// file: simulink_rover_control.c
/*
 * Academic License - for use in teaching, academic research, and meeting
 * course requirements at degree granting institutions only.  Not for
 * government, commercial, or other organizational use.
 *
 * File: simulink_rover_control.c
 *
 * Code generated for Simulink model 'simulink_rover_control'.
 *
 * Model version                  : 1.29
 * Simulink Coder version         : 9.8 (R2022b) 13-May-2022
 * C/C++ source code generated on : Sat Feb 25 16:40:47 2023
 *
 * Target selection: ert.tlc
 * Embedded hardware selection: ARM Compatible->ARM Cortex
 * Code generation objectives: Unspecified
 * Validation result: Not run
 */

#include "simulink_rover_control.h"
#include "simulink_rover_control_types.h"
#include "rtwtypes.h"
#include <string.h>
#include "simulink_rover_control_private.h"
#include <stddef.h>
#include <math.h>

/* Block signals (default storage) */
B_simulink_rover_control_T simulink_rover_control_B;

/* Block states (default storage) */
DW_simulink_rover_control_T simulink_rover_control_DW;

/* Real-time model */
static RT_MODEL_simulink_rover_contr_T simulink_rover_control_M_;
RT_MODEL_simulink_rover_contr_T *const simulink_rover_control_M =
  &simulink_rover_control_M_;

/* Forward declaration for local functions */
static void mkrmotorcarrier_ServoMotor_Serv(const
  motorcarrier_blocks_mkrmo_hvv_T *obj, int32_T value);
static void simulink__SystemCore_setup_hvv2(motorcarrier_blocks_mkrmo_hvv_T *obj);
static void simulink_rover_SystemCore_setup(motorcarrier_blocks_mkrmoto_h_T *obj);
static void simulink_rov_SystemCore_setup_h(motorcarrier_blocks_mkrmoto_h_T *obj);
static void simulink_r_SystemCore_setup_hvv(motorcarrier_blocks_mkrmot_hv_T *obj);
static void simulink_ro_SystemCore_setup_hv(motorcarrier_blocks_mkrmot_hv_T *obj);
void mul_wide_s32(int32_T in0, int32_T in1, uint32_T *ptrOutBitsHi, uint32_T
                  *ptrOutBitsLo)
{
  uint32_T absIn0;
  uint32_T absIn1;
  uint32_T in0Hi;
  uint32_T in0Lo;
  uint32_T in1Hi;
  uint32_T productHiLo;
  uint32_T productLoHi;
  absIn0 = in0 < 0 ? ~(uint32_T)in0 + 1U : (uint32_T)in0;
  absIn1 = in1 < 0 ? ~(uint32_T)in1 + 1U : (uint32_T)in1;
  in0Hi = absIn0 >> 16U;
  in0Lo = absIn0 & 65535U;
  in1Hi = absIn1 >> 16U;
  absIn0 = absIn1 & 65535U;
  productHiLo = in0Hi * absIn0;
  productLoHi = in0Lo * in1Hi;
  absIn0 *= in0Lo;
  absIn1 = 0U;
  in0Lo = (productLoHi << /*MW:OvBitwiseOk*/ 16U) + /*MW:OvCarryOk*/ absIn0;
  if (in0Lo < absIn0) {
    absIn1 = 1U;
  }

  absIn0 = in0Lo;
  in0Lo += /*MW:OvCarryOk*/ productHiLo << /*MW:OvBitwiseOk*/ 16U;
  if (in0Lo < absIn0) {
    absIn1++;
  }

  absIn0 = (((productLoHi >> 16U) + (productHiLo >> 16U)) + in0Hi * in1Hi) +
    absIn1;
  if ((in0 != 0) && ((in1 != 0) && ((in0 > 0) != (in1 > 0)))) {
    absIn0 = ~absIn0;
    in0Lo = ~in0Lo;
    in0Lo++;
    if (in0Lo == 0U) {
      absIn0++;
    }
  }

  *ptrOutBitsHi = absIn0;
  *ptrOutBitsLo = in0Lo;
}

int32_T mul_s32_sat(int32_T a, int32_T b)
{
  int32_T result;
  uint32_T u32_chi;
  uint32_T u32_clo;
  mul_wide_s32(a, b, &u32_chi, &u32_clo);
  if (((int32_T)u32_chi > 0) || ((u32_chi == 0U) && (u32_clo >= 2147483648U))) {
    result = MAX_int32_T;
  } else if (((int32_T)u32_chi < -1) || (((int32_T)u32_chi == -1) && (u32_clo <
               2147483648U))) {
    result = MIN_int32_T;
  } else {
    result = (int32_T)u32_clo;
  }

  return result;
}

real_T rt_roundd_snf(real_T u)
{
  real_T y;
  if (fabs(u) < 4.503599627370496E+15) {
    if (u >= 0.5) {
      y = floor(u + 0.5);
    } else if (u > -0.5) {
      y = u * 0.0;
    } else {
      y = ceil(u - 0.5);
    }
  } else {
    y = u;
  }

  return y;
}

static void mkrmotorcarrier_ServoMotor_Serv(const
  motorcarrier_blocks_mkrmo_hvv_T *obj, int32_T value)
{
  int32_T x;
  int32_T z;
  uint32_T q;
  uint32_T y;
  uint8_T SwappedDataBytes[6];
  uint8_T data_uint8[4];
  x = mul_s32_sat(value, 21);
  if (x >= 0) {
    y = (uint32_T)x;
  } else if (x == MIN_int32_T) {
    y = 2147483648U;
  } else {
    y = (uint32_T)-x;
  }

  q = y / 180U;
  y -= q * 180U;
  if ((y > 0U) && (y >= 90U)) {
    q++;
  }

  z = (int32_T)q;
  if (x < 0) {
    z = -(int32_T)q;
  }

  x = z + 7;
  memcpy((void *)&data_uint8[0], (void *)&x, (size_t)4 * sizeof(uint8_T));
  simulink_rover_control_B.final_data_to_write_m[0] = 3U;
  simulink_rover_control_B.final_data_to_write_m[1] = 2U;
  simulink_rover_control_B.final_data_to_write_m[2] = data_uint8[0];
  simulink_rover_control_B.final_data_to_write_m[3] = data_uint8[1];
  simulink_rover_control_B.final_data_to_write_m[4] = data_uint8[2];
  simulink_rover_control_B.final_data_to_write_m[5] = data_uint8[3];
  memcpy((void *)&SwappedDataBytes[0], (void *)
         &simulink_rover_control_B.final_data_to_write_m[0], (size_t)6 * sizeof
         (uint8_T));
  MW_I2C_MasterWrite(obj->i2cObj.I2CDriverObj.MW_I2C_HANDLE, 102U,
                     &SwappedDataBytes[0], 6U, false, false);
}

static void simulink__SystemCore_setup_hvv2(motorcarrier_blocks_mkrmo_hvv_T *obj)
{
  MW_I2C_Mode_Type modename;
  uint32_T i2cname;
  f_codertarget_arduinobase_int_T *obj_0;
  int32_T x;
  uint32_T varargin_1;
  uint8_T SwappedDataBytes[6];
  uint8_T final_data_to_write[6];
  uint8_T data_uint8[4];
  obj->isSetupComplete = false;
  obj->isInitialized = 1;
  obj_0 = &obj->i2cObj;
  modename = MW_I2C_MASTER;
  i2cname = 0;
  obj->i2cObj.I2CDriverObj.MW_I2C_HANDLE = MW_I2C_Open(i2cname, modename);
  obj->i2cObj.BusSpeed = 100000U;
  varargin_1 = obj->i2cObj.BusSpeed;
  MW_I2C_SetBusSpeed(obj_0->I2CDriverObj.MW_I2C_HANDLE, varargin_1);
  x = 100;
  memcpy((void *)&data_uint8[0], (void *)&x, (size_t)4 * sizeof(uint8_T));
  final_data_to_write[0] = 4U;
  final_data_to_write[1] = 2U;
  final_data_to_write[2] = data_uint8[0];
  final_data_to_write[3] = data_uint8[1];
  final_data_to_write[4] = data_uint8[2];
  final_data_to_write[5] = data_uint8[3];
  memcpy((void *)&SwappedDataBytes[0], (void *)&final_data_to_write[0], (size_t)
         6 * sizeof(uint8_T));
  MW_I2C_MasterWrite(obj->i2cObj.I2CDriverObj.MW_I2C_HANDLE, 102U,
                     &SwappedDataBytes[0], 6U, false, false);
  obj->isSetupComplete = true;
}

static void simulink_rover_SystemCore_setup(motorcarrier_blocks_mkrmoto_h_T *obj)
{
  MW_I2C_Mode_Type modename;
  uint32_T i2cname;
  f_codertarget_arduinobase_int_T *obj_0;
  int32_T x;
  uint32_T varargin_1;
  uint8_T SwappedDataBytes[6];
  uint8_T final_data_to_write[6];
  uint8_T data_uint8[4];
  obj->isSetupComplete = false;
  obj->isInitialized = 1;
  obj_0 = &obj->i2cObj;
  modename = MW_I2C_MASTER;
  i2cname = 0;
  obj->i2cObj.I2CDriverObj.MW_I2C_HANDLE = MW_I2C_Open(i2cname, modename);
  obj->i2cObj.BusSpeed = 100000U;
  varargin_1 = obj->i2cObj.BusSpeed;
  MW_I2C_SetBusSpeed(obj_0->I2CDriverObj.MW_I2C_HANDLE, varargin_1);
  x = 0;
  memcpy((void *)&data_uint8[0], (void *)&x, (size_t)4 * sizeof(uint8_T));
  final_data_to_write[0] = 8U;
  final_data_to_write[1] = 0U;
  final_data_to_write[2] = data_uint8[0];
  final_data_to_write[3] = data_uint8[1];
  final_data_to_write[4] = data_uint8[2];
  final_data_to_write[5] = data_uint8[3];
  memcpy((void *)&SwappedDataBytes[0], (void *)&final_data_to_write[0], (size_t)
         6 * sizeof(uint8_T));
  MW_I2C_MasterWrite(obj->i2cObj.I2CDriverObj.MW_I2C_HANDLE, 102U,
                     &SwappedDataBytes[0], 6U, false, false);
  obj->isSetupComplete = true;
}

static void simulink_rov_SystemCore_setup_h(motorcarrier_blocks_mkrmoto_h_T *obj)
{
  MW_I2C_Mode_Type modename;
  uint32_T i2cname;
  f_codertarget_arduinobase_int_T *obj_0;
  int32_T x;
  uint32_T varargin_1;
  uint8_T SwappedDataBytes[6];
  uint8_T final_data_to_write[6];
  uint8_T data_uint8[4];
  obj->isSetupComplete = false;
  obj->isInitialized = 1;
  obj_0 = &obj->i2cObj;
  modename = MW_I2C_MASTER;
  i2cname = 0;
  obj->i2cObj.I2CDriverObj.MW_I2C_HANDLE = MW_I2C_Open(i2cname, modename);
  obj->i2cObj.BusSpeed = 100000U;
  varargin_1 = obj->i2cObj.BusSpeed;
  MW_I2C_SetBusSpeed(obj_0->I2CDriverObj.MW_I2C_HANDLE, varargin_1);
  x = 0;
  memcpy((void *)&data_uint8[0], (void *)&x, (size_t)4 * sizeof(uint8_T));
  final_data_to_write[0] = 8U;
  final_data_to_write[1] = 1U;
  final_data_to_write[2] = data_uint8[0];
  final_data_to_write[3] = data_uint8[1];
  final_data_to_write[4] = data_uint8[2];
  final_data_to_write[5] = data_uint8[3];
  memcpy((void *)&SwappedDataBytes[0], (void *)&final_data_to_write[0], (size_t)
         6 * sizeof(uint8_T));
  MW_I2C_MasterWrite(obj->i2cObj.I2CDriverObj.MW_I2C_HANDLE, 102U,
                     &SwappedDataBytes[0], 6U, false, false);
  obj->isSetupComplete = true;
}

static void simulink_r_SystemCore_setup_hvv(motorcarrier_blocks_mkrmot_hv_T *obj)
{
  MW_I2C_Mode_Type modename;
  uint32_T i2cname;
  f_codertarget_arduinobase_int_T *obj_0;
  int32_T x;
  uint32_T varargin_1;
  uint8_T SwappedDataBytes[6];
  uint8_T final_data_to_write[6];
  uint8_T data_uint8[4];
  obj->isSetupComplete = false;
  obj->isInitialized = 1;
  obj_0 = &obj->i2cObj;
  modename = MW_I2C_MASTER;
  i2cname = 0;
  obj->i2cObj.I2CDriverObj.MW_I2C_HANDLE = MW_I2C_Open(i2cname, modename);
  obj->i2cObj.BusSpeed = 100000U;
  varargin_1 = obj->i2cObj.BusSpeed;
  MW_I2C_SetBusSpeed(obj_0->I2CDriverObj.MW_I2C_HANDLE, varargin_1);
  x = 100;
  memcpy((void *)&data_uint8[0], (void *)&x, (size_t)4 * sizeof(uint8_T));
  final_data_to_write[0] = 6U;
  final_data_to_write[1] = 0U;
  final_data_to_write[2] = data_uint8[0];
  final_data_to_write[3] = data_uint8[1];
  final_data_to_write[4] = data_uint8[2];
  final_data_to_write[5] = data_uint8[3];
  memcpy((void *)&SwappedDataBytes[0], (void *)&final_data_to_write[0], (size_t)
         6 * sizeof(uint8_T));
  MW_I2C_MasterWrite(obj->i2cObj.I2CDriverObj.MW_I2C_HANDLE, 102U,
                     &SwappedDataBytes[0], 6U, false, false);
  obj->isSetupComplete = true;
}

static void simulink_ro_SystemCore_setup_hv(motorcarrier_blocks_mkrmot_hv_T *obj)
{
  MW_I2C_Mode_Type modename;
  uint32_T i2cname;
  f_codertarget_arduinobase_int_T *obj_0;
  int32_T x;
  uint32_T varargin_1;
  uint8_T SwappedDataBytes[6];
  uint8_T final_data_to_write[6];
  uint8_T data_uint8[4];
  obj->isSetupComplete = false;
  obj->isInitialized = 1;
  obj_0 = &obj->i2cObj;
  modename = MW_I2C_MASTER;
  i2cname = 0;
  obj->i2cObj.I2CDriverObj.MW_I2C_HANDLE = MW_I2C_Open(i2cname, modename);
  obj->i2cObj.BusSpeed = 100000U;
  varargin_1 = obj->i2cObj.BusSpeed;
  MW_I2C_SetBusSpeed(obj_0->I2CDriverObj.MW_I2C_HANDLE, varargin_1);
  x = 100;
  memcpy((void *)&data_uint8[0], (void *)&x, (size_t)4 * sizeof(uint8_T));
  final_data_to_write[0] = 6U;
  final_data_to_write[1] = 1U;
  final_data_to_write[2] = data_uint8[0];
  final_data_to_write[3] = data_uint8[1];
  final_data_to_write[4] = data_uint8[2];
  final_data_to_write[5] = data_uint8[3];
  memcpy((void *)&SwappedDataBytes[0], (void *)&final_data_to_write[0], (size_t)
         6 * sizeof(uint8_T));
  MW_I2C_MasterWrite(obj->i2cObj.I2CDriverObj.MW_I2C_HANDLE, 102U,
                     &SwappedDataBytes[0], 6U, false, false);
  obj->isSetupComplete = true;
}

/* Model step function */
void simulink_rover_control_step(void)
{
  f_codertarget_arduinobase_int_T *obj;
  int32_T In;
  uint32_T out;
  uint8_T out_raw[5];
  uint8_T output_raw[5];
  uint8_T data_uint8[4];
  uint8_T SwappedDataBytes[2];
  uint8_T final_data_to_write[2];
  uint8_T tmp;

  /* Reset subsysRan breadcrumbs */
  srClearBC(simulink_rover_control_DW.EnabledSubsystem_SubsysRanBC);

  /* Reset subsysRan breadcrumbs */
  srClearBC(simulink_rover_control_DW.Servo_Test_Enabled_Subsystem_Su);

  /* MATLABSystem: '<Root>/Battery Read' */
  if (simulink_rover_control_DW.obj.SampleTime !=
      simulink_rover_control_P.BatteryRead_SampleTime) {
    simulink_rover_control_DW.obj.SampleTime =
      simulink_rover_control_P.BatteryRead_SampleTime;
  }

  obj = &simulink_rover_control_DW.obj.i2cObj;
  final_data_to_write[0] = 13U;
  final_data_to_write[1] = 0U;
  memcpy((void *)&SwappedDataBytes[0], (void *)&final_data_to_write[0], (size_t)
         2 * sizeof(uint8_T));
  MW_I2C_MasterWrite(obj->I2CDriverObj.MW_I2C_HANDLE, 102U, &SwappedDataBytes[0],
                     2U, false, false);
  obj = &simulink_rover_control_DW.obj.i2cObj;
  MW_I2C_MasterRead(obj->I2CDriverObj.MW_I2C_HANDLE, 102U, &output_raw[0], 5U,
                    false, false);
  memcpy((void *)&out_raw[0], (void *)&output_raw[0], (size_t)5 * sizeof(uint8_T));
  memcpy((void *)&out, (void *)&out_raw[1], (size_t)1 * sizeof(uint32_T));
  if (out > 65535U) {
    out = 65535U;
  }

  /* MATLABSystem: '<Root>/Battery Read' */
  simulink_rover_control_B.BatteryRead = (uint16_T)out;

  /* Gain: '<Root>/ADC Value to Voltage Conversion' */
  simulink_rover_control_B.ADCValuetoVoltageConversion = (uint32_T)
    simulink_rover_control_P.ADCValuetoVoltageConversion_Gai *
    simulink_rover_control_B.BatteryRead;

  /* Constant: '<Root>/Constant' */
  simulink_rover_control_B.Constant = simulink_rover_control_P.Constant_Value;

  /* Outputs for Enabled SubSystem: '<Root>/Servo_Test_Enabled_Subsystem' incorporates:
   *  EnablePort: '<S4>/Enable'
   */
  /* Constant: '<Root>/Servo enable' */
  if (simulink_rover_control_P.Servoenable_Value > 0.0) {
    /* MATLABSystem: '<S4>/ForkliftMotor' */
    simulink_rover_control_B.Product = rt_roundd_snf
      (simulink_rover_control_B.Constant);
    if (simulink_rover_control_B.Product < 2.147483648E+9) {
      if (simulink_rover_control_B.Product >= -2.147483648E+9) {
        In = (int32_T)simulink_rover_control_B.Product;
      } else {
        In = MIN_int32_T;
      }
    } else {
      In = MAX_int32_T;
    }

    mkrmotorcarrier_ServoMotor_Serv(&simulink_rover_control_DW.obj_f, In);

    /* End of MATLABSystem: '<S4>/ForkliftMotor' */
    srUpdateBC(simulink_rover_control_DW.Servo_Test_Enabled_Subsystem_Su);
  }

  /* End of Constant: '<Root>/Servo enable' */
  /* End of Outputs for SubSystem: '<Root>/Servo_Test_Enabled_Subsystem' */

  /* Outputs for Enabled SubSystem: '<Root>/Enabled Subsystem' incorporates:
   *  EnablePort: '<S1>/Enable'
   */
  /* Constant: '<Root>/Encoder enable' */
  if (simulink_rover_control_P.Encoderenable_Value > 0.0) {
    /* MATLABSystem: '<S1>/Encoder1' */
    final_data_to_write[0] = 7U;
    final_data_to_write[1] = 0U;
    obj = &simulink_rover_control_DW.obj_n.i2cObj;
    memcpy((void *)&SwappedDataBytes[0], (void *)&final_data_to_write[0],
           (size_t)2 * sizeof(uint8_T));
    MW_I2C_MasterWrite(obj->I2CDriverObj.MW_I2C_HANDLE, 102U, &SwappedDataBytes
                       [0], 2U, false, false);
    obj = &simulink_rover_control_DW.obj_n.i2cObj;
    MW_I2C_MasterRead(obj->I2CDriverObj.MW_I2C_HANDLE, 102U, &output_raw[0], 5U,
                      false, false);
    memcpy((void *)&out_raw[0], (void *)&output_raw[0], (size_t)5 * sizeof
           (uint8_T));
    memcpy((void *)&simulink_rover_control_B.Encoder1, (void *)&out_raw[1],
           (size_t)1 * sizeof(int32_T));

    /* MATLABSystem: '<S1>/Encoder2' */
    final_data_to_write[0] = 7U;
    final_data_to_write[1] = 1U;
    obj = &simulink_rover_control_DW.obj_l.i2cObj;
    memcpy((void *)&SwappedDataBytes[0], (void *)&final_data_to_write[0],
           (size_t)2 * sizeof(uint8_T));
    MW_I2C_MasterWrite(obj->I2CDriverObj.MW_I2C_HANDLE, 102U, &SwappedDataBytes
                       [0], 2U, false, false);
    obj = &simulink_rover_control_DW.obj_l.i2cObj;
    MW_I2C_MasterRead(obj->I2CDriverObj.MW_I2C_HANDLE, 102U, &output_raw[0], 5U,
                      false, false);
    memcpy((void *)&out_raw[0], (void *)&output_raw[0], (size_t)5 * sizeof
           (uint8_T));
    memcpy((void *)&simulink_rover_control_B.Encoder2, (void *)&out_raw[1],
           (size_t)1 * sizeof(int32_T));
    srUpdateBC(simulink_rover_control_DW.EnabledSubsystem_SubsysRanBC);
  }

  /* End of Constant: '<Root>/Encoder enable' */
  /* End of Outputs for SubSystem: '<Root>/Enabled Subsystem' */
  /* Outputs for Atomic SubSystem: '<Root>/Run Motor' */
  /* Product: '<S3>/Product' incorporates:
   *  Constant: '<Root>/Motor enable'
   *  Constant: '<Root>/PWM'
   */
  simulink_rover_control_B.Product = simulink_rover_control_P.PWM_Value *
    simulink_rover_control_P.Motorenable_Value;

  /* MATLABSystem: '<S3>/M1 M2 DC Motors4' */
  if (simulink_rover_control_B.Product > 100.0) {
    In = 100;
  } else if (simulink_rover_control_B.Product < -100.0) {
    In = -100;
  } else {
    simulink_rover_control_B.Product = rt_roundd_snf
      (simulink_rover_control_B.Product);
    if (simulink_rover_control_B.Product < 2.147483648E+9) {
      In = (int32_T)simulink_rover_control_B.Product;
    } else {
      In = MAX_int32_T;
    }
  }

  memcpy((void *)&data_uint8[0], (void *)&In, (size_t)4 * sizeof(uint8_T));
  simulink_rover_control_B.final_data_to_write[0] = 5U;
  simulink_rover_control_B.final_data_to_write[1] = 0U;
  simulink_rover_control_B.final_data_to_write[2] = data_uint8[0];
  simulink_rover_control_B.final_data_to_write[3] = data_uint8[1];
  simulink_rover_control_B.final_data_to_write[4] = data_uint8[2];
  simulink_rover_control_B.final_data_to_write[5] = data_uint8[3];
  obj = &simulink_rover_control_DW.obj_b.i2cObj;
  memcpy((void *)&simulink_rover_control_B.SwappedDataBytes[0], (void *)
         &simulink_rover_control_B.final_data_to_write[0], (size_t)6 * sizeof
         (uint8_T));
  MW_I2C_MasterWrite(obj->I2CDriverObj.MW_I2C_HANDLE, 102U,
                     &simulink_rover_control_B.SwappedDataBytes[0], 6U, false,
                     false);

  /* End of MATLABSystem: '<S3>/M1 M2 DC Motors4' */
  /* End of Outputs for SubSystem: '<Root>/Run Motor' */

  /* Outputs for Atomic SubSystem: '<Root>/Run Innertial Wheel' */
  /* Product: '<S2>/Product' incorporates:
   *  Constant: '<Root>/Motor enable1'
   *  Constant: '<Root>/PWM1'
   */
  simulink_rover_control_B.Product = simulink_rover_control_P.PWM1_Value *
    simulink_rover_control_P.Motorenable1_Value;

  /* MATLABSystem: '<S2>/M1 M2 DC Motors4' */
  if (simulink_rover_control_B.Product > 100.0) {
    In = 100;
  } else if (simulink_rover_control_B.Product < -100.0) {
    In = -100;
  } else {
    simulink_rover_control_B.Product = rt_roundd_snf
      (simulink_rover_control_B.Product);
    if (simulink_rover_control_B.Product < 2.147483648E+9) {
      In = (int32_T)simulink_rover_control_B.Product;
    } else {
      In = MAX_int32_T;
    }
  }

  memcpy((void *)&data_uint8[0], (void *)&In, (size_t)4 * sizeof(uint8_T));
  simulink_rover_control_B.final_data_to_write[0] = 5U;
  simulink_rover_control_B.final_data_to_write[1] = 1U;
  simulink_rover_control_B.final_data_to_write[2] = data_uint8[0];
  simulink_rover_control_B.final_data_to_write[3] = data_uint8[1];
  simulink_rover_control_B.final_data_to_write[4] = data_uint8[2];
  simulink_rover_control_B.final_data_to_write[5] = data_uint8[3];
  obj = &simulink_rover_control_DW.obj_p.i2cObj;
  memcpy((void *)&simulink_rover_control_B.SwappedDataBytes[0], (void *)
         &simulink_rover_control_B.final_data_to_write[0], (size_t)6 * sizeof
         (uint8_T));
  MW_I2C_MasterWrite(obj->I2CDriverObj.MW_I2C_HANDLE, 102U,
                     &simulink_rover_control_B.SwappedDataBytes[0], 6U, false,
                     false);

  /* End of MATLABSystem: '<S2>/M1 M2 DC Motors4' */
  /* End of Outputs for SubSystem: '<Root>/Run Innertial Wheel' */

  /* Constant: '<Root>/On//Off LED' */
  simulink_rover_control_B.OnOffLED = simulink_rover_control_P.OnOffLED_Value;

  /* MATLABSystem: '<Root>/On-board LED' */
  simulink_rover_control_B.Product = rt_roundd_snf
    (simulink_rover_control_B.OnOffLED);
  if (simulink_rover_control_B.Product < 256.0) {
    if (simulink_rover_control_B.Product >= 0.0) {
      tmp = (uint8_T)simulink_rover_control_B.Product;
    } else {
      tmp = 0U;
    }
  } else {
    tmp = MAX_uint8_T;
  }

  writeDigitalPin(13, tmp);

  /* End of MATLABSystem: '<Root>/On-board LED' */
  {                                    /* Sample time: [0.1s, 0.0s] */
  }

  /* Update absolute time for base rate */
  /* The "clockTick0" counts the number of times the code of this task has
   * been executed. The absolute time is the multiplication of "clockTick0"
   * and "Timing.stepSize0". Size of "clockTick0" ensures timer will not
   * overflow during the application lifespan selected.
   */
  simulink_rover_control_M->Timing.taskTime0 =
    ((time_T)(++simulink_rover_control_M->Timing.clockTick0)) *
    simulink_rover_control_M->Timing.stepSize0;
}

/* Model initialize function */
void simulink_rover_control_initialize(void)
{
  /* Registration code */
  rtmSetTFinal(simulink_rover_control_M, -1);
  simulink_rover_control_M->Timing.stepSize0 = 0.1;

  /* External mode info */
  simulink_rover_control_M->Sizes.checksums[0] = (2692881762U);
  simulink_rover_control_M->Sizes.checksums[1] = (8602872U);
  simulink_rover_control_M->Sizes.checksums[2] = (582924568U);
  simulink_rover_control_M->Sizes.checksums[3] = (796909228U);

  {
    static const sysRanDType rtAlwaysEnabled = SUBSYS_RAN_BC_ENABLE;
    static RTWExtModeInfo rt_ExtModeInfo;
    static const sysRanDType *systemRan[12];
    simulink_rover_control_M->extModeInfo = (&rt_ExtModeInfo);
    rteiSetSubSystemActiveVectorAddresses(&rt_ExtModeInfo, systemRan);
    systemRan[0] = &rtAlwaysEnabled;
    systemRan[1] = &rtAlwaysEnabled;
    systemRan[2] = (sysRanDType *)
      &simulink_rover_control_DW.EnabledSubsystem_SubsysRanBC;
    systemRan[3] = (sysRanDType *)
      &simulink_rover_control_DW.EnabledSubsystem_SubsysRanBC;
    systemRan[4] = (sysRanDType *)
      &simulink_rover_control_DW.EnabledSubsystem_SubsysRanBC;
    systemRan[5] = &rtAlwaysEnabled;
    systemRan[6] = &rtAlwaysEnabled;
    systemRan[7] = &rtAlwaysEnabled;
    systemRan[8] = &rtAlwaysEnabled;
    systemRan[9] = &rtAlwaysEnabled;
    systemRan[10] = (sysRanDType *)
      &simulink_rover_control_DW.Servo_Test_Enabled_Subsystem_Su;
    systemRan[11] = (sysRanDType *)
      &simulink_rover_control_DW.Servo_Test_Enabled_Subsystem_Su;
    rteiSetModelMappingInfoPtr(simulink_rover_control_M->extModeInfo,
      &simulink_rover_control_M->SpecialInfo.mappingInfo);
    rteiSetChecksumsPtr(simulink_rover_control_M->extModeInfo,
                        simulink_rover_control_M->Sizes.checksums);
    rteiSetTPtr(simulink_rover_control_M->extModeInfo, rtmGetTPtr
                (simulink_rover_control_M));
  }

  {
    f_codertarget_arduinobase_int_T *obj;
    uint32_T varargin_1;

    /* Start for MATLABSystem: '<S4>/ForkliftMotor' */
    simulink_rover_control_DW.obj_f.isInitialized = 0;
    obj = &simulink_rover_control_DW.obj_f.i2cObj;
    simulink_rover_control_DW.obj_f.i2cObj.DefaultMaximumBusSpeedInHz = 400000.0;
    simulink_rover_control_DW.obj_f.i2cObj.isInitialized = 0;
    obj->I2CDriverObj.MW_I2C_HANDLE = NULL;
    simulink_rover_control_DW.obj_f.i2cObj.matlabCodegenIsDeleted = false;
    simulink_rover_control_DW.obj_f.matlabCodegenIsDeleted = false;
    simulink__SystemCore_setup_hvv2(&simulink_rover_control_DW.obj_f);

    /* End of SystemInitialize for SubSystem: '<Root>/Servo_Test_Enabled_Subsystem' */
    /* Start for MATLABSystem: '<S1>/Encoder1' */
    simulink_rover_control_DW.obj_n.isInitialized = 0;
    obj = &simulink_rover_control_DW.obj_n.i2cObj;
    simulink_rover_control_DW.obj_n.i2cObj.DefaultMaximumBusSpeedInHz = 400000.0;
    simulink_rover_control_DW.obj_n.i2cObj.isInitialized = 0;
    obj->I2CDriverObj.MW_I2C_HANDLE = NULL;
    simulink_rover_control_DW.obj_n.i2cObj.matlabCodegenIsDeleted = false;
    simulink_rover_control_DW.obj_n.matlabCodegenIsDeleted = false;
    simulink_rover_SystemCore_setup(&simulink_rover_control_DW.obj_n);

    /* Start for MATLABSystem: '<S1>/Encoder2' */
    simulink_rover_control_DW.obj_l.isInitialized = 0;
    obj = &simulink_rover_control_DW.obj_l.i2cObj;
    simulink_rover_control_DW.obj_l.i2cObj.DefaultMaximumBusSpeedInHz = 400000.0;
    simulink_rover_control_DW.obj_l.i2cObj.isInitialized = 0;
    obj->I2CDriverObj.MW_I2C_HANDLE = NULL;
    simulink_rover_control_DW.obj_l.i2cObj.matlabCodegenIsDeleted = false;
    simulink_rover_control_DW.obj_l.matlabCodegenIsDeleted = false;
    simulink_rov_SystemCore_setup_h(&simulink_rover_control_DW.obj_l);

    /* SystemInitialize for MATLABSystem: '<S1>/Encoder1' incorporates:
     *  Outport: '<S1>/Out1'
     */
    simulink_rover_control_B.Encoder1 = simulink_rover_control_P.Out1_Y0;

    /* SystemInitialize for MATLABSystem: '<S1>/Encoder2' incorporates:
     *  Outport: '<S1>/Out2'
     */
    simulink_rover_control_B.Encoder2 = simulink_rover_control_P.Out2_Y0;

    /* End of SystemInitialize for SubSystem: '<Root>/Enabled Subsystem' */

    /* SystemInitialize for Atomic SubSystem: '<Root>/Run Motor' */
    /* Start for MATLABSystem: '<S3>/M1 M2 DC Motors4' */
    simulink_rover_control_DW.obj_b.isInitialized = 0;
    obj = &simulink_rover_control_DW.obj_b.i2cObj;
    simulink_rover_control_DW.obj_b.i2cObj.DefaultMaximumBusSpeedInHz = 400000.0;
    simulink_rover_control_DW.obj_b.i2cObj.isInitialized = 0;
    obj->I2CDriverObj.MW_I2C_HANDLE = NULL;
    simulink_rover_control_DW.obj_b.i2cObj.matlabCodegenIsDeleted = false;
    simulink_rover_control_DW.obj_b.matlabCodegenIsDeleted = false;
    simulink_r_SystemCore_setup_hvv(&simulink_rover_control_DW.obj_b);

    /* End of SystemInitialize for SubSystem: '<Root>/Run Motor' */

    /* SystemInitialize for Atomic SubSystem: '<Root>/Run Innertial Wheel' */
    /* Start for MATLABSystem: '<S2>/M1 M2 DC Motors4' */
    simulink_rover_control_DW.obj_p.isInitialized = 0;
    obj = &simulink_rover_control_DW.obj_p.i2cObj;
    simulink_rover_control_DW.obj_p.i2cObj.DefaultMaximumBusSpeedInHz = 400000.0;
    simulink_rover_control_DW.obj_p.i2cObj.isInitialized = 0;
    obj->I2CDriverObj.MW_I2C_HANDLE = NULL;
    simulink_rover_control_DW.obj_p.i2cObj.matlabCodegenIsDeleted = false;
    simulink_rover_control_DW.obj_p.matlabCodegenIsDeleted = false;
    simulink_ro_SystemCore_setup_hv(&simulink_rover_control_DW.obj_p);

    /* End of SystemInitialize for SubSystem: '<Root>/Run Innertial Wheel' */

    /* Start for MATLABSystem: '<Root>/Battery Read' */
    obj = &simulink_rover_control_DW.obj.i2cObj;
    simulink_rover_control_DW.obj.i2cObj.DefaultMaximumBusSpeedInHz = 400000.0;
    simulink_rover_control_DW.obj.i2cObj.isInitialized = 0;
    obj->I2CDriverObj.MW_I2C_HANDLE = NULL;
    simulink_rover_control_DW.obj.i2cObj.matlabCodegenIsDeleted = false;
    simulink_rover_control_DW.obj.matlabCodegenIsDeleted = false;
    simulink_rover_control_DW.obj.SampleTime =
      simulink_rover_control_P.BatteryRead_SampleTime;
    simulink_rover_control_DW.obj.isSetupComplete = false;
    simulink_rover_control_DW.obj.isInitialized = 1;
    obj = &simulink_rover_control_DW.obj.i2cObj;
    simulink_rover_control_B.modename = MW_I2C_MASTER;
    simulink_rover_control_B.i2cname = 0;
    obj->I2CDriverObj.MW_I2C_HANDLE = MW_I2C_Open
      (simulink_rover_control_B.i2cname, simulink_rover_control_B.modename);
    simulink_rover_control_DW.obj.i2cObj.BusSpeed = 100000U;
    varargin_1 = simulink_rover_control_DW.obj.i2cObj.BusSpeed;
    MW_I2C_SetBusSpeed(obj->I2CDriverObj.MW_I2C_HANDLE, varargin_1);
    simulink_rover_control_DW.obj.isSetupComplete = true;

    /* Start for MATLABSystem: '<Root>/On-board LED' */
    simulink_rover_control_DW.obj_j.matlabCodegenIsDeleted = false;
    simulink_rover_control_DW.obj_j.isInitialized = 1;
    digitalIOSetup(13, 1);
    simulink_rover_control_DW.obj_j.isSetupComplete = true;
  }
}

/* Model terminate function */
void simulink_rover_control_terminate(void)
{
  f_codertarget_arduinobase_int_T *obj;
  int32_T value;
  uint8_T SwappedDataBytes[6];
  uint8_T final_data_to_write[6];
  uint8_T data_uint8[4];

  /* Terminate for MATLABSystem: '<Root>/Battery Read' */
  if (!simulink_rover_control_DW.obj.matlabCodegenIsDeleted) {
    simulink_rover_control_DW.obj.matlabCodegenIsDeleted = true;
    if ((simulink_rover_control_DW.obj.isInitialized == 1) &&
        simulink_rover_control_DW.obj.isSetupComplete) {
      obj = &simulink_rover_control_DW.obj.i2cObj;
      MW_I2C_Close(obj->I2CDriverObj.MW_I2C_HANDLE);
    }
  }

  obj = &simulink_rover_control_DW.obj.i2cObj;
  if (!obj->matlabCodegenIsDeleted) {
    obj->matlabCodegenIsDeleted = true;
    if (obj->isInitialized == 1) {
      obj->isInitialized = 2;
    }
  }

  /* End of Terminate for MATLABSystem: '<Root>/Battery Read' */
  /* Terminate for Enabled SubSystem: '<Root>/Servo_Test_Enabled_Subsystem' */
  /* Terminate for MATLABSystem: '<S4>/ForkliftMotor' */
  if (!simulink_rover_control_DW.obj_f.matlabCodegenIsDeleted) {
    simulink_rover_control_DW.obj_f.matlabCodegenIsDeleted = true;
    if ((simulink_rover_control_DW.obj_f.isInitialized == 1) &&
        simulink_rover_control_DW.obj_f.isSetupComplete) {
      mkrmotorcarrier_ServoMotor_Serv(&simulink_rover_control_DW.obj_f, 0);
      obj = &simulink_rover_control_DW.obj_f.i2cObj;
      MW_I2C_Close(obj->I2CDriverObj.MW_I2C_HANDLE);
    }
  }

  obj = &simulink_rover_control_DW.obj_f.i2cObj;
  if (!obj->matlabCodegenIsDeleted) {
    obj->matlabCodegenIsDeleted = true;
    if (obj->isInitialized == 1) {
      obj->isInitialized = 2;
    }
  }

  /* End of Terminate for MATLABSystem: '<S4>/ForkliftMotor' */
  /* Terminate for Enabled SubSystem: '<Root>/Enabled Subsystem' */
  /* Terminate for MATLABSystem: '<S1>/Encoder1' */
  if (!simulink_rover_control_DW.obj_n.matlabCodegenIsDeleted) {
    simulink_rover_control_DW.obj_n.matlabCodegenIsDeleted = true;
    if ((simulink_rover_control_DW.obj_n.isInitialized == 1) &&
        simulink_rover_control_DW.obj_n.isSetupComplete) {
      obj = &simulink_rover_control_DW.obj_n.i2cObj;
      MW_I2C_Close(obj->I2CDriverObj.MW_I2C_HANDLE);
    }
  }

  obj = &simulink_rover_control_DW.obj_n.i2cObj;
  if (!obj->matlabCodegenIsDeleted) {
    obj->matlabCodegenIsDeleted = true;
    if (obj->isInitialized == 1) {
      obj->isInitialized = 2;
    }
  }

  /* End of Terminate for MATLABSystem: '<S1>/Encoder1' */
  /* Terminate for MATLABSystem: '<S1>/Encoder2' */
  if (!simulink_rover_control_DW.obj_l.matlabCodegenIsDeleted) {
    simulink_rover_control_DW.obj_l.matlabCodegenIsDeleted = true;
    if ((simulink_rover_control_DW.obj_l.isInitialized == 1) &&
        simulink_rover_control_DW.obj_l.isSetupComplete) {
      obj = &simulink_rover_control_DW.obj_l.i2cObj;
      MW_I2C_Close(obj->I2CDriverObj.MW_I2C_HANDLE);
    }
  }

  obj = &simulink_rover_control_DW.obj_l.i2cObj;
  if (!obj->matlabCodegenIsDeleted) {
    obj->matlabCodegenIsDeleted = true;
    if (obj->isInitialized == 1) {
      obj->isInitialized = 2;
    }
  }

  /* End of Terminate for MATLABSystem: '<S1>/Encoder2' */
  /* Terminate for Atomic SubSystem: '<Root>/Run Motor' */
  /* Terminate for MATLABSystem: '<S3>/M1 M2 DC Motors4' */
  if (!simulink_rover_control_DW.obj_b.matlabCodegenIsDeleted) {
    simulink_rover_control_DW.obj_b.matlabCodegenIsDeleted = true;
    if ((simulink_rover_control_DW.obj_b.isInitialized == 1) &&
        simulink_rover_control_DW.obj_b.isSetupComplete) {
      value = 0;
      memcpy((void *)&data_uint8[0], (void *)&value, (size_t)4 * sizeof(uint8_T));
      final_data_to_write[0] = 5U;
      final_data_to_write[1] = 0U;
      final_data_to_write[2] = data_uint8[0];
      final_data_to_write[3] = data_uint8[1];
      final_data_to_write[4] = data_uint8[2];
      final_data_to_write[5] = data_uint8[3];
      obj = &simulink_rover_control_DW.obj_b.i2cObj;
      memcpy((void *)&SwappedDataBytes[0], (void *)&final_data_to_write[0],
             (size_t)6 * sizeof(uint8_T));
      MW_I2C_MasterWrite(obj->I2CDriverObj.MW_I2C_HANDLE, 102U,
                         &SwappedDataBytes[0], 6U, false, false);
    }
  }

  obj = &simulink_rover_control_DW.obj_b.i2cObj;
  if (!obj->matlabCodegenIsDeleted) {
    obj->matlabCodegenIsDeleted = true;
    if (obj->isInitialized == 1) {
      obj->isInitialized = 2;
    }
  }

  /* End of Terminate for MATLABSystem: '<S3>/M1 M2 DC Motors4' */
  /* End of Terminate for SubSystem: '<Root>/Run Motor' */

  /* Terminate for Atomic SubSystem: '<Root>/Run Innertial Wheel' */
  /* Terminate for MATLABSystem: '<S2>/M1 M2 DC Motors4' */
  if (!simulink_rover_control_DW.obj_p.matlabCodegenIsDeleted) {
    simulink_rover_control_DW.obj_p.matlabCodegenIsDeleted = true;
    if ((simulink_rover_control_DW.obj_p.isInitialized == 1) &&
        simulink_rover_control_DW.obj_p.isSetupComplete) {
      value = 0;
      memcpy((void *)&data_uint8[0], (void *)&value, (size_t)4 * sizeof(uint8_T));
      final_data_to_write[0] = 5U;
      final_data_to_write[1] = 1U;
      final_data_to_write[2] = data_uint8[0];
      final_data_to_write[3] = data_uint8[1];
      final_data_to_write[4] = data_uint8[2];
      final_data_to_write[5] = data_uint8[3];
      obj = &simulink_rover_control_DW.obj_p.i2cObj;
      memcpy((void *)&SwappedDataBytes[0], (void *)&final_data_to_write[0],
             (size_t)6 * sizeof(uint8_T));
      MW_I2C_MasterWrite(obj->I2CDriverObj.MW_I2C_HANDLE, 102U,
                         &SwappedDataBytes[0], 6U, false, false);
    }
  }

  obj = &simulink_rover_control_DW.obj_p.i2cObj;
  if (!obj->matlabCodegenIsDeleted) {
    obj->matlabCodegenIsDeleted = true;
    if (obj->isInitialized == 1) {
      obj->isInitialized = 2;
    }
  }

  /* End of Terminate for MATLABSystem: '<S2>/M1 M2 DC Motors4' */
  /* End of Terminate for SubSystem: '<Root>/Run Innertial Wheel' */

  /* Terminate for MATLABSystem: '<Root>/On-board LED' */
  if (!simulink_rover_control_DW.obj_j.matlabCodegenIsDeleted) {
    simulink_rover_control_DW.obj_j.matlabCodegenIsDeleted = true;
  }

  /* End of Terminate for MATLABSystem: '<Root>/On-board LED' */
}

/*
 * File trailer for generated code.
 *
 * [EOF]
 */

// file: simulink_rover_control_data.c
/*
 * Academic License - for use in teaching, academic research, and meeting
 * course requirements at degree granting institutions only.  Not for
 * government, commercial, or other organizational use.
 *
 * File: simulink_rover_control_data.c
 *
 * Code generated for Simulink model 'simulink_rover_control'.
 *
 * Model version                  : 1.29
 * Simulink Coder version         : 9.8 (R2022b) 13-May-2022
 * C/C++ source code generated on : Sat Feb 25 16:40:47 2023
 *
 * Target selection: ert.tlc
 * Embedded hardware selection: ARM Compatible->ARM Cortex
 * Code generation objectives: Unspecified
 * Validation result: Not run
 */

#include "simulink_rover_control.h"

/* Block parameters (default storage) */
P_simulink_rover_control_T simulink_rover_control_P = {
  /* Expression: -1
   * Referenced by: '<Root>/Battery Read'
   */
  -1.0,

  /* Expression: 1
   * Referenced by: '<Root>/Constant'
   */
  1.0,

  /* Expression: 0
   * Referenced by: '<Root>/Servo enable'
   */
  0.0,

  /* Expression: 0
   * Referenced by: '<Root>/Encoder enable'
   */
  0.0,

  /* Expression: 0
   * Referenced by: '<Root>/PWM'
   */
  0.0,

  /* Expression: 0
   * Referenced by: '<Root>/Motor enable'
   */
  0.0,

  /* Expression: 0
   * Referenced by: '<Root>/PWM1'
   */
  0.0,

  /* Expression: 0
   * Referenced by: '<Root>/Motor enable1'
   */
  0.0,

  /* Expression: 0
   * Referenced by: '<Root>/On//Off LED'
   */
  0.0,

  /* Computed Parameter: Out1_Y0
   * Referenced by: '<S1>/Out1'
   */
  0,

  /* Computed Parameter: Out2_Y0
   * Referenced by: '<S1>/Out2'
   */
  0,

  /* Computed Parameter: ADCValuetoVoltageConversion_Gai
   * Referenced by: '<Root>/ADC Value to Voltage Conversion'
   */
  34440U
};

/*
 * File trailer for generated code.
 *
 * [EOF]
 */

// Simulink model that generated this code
simulink model "simulink_rover_control"  (R2021b)
settings: Solver=FixedStepAuto  StartTime=0.0  StopTime=inf  RelTol=1e-3  EnableMultiTasking=on
model workspace (MAT data in the model file):
  ON = 1
libraries: arduinomotorcarrierlib x6, arduinolib x1

== system simulink_rover_control ==
  note: The various models and dashboard elements included here will help you test out the general functioning of various hardware components of the Arduino Engineering kit Rev2.
      |
      | Steps to run the model:
      | Assemble the bare bone components - Arduino Nano 33 IoT board + Nano Motor Carrier + 2 Micro DC motors + Servo Motor following instructions in the documentation
      | Ensure the motors/wheels or the servo motor is lifted off the ground
      | Connect the Arduino board to your host computer (PC or Laptop) via USB cable
      | Under the hardware tab in Simulink ensure the Arduino Nano 33 IoT board is selected and run the model in monitor & tune mode
      | Enable or disable certain sections using the provided slider switches and inspect if the components are functioning properly
      |
      | Troubleshooting:
      | If you face an error with board connection, open the hardware settings, under Target hardware resources and Host-board connection choose Set host COM port Manually. Enter the COM port number of the Arduino board.
      | You can also use the LEDs on the Nano motor carrier board as a way of identifying the effective functioning of the driver board without connecting the motors
      | This model assumes the DC motors are connected to M1 & M2 of the Nano Motor Carrier Board and Servo is connected to port 3. Modify the ports accordingly by double-clicking each model if required.
  note: Arduino Engineering Kit Test Model for Rover Project
  note: Motor Movements Model
  note: Encoder Value Read Model
  note: Battery Voltage Read Model
  note: Servo Motor Model
  note: LED Control Model
  note: Encoder Value
  note: 2nd Geared DC Motor Movement
  note: Servo Motor Movements
  note: Battery Voltage
  note: Built-in LED
  note: Copyright 2022 The MathWorks, Inc.
  note: Motor Movements Model
  note: 1st Geared DC Motor Movement
  1st Geared DC Motor Encoder : DisplayBlock  LabelPosition=Hide  Format=short  Transparency=1
  2nd Geared DC Motor Encoder : DisplayBlock  LabelPosition=Hide  Format=short  Transparency=1
  ADC Value to Voltage Conversion : Gain  Gain=4.2/1023
  Battery Read : arduinomotorcarrierlib/Battery Read  SlaveAddress=uint8( hex2dec( '66' ) )  blockPlatform=ARDUINO  SampleTime=-1
  Constant : Constant
  Display : Display
  Display1 : Display
  Enabled Subsystem : Subsystem  TreatAsAtomicUnit=on
  Encoder 1 : Display
  Encoder 2 : Display
  Encoder enable : Constant  Value=0
  Lamp : LampBlock  LabelPosition=Hide
  Motor enable : Constant  Value=0
  Motor enable1 : Constant  Value=0
  On-board LED : arduinolib/Digital Output  pinNumber=13  Direction=output  blockPlatform=arduino
  On/Off LED : Constant  Value=0
  PWM : Constant  Value=0
  PWM Slider : SliderBlock  ScaleMin=-50  ScaleMax=50  TickInterval=10
  PWM Slider1 : SliderBlock  ScaleMin=-50  ScaleMax=50  TickInterval=10
  PWM1 : Constant  Value=0
  Radio Button : RadioButtonGroup  SelectedLabel=Turn Off  ButtonGroupName=Control the LED
  Run Innertial Wheel : Subsystem  TreatAsAtomicUnit=on
  Run Motor : Subsystem  TreatAsAtomicUnit=on
  Servo Shaft Position Slider : SliderBlock  ScaleMin=-15  ScaleMax=25  TickInterval=2
  Servo enable : Constant  Value=0
  Servo_Test_Enabled_Subsystem : Subsystem  TreatAsAtomicUnit=on
  Slider Switch{,1..3} (4 alike) : SliderSwitchBlock
  Value in Volts : QuarterGaugeBlock  ScaleMin=3  ScaleMax=4.2  TickInterval=0.2
  wires:
  ADC Value to Voltage Conversion/1 -> Display/1
  Battery Read/1 -> Display1/1, ADC Value to Voltage Conversion/1
  Encoder enable/1 -> Enabled Subsystem/Enable
  Enabled Subsystem/1(Out1) -> Encoder 1/1
  Enabled Subsystem/2(Out2) -> Encoder 2/1
  Servo enable/1 -> Servo_Test_Enabled_Subsystem/Enable
  On/Off LED/1 -> On-board LED/1
  Constant/1 -> Servo_Test_Enabled_Subsystem/1(Shaft Position)
  PWM/1 -> Run Motor/1(PWM Value)
  Motor enable/1 -> Run Motor/2(Motor Enable)
  Motor enable1/1 -> Run Innertial Wheel/2(Motor Enable)
  PWM1/1 -> Run Innertial Wheel/1(PWM Value)

== system simulink_rover_control/Enabled Subsystem ==
  Enable : EnablePort
  Encoder1 : arduinomotorcarrierlib/Encoder  SlaveAddress=uint8( hex2dec( '66' ) )  blockPlatform=ARDUINO  Encoder=1  ShowSpeed=off  ResetOption=on  SampleTime=0.1
  Encoder2 : arduinomotorcarrierlib/Encoder  SlaveAddress=uint8( hex2dec( '66' ) )  blockPlatform=ARDUINO  Encoder=2  ShowSpeed=off  ResetOption=on  SampleTime=0.1
  Out1 : Outport
  Out2 : Outport  Port=2
  wires:
  Encoder1/1 -> Out1/1
  Encoder2/1 -> Out2/1

== system simulink_rover_control/Run Innertial Wheel ==
  PWM Value : Inport
  Motor Enable : Inport  Port=2
  M1 M2 DC Motors4 : arduinomotorcarrierlib/M1 M2 DC Motors  SlaveAddress=uint8( hex2dec( '66' ) )  blockPlatform=ARDUINO  MotorNumber=M2  MotorCarrierPWMFreq=100
  Product : Product
  wires:
  Product/1 -> M1 M2 DC Motors4/1
  PWM Value/1 -> Product/1
  Motor Enable/1 -> Product/2

== system simulink_rover_control/Run Motor ==
  PWM Value : Inport
  Motor Enable : Inport  Port=2
  M1 M2 DC Motors4 : arduinomotorcarrierlib/M1 M2 DC Motors  SlaveAddress=uint8( hex2dec( '66' ) )  blockPlatform=ARDUINO  MotorNumber=M1  MotorCarrierPWMFreq=100
  Product : Product
  wires:
  Product/1 -> M1 M2 DC Motors4/1
  PWM Value/1 -> Product/1
  Motor Enable/1 -> Product/2

== system simulink_rover_control/Servo_Test_Enabled_Subsystem ==
  Shaft Position : Inport
  Enable : EnablePort
  ForkliftMotor : arduinomotorcarrierlib/Servo Write  SlaveAddress=uint8( hex2dec( '66' ) )  blockPlatform=ARDUINO  MotorNumber=3  MotorCarrierPWMFreq=100
  Scope : Scope
  wires:
  Shaft Position/1 -> Scope/1, ForkliftMotor/1
